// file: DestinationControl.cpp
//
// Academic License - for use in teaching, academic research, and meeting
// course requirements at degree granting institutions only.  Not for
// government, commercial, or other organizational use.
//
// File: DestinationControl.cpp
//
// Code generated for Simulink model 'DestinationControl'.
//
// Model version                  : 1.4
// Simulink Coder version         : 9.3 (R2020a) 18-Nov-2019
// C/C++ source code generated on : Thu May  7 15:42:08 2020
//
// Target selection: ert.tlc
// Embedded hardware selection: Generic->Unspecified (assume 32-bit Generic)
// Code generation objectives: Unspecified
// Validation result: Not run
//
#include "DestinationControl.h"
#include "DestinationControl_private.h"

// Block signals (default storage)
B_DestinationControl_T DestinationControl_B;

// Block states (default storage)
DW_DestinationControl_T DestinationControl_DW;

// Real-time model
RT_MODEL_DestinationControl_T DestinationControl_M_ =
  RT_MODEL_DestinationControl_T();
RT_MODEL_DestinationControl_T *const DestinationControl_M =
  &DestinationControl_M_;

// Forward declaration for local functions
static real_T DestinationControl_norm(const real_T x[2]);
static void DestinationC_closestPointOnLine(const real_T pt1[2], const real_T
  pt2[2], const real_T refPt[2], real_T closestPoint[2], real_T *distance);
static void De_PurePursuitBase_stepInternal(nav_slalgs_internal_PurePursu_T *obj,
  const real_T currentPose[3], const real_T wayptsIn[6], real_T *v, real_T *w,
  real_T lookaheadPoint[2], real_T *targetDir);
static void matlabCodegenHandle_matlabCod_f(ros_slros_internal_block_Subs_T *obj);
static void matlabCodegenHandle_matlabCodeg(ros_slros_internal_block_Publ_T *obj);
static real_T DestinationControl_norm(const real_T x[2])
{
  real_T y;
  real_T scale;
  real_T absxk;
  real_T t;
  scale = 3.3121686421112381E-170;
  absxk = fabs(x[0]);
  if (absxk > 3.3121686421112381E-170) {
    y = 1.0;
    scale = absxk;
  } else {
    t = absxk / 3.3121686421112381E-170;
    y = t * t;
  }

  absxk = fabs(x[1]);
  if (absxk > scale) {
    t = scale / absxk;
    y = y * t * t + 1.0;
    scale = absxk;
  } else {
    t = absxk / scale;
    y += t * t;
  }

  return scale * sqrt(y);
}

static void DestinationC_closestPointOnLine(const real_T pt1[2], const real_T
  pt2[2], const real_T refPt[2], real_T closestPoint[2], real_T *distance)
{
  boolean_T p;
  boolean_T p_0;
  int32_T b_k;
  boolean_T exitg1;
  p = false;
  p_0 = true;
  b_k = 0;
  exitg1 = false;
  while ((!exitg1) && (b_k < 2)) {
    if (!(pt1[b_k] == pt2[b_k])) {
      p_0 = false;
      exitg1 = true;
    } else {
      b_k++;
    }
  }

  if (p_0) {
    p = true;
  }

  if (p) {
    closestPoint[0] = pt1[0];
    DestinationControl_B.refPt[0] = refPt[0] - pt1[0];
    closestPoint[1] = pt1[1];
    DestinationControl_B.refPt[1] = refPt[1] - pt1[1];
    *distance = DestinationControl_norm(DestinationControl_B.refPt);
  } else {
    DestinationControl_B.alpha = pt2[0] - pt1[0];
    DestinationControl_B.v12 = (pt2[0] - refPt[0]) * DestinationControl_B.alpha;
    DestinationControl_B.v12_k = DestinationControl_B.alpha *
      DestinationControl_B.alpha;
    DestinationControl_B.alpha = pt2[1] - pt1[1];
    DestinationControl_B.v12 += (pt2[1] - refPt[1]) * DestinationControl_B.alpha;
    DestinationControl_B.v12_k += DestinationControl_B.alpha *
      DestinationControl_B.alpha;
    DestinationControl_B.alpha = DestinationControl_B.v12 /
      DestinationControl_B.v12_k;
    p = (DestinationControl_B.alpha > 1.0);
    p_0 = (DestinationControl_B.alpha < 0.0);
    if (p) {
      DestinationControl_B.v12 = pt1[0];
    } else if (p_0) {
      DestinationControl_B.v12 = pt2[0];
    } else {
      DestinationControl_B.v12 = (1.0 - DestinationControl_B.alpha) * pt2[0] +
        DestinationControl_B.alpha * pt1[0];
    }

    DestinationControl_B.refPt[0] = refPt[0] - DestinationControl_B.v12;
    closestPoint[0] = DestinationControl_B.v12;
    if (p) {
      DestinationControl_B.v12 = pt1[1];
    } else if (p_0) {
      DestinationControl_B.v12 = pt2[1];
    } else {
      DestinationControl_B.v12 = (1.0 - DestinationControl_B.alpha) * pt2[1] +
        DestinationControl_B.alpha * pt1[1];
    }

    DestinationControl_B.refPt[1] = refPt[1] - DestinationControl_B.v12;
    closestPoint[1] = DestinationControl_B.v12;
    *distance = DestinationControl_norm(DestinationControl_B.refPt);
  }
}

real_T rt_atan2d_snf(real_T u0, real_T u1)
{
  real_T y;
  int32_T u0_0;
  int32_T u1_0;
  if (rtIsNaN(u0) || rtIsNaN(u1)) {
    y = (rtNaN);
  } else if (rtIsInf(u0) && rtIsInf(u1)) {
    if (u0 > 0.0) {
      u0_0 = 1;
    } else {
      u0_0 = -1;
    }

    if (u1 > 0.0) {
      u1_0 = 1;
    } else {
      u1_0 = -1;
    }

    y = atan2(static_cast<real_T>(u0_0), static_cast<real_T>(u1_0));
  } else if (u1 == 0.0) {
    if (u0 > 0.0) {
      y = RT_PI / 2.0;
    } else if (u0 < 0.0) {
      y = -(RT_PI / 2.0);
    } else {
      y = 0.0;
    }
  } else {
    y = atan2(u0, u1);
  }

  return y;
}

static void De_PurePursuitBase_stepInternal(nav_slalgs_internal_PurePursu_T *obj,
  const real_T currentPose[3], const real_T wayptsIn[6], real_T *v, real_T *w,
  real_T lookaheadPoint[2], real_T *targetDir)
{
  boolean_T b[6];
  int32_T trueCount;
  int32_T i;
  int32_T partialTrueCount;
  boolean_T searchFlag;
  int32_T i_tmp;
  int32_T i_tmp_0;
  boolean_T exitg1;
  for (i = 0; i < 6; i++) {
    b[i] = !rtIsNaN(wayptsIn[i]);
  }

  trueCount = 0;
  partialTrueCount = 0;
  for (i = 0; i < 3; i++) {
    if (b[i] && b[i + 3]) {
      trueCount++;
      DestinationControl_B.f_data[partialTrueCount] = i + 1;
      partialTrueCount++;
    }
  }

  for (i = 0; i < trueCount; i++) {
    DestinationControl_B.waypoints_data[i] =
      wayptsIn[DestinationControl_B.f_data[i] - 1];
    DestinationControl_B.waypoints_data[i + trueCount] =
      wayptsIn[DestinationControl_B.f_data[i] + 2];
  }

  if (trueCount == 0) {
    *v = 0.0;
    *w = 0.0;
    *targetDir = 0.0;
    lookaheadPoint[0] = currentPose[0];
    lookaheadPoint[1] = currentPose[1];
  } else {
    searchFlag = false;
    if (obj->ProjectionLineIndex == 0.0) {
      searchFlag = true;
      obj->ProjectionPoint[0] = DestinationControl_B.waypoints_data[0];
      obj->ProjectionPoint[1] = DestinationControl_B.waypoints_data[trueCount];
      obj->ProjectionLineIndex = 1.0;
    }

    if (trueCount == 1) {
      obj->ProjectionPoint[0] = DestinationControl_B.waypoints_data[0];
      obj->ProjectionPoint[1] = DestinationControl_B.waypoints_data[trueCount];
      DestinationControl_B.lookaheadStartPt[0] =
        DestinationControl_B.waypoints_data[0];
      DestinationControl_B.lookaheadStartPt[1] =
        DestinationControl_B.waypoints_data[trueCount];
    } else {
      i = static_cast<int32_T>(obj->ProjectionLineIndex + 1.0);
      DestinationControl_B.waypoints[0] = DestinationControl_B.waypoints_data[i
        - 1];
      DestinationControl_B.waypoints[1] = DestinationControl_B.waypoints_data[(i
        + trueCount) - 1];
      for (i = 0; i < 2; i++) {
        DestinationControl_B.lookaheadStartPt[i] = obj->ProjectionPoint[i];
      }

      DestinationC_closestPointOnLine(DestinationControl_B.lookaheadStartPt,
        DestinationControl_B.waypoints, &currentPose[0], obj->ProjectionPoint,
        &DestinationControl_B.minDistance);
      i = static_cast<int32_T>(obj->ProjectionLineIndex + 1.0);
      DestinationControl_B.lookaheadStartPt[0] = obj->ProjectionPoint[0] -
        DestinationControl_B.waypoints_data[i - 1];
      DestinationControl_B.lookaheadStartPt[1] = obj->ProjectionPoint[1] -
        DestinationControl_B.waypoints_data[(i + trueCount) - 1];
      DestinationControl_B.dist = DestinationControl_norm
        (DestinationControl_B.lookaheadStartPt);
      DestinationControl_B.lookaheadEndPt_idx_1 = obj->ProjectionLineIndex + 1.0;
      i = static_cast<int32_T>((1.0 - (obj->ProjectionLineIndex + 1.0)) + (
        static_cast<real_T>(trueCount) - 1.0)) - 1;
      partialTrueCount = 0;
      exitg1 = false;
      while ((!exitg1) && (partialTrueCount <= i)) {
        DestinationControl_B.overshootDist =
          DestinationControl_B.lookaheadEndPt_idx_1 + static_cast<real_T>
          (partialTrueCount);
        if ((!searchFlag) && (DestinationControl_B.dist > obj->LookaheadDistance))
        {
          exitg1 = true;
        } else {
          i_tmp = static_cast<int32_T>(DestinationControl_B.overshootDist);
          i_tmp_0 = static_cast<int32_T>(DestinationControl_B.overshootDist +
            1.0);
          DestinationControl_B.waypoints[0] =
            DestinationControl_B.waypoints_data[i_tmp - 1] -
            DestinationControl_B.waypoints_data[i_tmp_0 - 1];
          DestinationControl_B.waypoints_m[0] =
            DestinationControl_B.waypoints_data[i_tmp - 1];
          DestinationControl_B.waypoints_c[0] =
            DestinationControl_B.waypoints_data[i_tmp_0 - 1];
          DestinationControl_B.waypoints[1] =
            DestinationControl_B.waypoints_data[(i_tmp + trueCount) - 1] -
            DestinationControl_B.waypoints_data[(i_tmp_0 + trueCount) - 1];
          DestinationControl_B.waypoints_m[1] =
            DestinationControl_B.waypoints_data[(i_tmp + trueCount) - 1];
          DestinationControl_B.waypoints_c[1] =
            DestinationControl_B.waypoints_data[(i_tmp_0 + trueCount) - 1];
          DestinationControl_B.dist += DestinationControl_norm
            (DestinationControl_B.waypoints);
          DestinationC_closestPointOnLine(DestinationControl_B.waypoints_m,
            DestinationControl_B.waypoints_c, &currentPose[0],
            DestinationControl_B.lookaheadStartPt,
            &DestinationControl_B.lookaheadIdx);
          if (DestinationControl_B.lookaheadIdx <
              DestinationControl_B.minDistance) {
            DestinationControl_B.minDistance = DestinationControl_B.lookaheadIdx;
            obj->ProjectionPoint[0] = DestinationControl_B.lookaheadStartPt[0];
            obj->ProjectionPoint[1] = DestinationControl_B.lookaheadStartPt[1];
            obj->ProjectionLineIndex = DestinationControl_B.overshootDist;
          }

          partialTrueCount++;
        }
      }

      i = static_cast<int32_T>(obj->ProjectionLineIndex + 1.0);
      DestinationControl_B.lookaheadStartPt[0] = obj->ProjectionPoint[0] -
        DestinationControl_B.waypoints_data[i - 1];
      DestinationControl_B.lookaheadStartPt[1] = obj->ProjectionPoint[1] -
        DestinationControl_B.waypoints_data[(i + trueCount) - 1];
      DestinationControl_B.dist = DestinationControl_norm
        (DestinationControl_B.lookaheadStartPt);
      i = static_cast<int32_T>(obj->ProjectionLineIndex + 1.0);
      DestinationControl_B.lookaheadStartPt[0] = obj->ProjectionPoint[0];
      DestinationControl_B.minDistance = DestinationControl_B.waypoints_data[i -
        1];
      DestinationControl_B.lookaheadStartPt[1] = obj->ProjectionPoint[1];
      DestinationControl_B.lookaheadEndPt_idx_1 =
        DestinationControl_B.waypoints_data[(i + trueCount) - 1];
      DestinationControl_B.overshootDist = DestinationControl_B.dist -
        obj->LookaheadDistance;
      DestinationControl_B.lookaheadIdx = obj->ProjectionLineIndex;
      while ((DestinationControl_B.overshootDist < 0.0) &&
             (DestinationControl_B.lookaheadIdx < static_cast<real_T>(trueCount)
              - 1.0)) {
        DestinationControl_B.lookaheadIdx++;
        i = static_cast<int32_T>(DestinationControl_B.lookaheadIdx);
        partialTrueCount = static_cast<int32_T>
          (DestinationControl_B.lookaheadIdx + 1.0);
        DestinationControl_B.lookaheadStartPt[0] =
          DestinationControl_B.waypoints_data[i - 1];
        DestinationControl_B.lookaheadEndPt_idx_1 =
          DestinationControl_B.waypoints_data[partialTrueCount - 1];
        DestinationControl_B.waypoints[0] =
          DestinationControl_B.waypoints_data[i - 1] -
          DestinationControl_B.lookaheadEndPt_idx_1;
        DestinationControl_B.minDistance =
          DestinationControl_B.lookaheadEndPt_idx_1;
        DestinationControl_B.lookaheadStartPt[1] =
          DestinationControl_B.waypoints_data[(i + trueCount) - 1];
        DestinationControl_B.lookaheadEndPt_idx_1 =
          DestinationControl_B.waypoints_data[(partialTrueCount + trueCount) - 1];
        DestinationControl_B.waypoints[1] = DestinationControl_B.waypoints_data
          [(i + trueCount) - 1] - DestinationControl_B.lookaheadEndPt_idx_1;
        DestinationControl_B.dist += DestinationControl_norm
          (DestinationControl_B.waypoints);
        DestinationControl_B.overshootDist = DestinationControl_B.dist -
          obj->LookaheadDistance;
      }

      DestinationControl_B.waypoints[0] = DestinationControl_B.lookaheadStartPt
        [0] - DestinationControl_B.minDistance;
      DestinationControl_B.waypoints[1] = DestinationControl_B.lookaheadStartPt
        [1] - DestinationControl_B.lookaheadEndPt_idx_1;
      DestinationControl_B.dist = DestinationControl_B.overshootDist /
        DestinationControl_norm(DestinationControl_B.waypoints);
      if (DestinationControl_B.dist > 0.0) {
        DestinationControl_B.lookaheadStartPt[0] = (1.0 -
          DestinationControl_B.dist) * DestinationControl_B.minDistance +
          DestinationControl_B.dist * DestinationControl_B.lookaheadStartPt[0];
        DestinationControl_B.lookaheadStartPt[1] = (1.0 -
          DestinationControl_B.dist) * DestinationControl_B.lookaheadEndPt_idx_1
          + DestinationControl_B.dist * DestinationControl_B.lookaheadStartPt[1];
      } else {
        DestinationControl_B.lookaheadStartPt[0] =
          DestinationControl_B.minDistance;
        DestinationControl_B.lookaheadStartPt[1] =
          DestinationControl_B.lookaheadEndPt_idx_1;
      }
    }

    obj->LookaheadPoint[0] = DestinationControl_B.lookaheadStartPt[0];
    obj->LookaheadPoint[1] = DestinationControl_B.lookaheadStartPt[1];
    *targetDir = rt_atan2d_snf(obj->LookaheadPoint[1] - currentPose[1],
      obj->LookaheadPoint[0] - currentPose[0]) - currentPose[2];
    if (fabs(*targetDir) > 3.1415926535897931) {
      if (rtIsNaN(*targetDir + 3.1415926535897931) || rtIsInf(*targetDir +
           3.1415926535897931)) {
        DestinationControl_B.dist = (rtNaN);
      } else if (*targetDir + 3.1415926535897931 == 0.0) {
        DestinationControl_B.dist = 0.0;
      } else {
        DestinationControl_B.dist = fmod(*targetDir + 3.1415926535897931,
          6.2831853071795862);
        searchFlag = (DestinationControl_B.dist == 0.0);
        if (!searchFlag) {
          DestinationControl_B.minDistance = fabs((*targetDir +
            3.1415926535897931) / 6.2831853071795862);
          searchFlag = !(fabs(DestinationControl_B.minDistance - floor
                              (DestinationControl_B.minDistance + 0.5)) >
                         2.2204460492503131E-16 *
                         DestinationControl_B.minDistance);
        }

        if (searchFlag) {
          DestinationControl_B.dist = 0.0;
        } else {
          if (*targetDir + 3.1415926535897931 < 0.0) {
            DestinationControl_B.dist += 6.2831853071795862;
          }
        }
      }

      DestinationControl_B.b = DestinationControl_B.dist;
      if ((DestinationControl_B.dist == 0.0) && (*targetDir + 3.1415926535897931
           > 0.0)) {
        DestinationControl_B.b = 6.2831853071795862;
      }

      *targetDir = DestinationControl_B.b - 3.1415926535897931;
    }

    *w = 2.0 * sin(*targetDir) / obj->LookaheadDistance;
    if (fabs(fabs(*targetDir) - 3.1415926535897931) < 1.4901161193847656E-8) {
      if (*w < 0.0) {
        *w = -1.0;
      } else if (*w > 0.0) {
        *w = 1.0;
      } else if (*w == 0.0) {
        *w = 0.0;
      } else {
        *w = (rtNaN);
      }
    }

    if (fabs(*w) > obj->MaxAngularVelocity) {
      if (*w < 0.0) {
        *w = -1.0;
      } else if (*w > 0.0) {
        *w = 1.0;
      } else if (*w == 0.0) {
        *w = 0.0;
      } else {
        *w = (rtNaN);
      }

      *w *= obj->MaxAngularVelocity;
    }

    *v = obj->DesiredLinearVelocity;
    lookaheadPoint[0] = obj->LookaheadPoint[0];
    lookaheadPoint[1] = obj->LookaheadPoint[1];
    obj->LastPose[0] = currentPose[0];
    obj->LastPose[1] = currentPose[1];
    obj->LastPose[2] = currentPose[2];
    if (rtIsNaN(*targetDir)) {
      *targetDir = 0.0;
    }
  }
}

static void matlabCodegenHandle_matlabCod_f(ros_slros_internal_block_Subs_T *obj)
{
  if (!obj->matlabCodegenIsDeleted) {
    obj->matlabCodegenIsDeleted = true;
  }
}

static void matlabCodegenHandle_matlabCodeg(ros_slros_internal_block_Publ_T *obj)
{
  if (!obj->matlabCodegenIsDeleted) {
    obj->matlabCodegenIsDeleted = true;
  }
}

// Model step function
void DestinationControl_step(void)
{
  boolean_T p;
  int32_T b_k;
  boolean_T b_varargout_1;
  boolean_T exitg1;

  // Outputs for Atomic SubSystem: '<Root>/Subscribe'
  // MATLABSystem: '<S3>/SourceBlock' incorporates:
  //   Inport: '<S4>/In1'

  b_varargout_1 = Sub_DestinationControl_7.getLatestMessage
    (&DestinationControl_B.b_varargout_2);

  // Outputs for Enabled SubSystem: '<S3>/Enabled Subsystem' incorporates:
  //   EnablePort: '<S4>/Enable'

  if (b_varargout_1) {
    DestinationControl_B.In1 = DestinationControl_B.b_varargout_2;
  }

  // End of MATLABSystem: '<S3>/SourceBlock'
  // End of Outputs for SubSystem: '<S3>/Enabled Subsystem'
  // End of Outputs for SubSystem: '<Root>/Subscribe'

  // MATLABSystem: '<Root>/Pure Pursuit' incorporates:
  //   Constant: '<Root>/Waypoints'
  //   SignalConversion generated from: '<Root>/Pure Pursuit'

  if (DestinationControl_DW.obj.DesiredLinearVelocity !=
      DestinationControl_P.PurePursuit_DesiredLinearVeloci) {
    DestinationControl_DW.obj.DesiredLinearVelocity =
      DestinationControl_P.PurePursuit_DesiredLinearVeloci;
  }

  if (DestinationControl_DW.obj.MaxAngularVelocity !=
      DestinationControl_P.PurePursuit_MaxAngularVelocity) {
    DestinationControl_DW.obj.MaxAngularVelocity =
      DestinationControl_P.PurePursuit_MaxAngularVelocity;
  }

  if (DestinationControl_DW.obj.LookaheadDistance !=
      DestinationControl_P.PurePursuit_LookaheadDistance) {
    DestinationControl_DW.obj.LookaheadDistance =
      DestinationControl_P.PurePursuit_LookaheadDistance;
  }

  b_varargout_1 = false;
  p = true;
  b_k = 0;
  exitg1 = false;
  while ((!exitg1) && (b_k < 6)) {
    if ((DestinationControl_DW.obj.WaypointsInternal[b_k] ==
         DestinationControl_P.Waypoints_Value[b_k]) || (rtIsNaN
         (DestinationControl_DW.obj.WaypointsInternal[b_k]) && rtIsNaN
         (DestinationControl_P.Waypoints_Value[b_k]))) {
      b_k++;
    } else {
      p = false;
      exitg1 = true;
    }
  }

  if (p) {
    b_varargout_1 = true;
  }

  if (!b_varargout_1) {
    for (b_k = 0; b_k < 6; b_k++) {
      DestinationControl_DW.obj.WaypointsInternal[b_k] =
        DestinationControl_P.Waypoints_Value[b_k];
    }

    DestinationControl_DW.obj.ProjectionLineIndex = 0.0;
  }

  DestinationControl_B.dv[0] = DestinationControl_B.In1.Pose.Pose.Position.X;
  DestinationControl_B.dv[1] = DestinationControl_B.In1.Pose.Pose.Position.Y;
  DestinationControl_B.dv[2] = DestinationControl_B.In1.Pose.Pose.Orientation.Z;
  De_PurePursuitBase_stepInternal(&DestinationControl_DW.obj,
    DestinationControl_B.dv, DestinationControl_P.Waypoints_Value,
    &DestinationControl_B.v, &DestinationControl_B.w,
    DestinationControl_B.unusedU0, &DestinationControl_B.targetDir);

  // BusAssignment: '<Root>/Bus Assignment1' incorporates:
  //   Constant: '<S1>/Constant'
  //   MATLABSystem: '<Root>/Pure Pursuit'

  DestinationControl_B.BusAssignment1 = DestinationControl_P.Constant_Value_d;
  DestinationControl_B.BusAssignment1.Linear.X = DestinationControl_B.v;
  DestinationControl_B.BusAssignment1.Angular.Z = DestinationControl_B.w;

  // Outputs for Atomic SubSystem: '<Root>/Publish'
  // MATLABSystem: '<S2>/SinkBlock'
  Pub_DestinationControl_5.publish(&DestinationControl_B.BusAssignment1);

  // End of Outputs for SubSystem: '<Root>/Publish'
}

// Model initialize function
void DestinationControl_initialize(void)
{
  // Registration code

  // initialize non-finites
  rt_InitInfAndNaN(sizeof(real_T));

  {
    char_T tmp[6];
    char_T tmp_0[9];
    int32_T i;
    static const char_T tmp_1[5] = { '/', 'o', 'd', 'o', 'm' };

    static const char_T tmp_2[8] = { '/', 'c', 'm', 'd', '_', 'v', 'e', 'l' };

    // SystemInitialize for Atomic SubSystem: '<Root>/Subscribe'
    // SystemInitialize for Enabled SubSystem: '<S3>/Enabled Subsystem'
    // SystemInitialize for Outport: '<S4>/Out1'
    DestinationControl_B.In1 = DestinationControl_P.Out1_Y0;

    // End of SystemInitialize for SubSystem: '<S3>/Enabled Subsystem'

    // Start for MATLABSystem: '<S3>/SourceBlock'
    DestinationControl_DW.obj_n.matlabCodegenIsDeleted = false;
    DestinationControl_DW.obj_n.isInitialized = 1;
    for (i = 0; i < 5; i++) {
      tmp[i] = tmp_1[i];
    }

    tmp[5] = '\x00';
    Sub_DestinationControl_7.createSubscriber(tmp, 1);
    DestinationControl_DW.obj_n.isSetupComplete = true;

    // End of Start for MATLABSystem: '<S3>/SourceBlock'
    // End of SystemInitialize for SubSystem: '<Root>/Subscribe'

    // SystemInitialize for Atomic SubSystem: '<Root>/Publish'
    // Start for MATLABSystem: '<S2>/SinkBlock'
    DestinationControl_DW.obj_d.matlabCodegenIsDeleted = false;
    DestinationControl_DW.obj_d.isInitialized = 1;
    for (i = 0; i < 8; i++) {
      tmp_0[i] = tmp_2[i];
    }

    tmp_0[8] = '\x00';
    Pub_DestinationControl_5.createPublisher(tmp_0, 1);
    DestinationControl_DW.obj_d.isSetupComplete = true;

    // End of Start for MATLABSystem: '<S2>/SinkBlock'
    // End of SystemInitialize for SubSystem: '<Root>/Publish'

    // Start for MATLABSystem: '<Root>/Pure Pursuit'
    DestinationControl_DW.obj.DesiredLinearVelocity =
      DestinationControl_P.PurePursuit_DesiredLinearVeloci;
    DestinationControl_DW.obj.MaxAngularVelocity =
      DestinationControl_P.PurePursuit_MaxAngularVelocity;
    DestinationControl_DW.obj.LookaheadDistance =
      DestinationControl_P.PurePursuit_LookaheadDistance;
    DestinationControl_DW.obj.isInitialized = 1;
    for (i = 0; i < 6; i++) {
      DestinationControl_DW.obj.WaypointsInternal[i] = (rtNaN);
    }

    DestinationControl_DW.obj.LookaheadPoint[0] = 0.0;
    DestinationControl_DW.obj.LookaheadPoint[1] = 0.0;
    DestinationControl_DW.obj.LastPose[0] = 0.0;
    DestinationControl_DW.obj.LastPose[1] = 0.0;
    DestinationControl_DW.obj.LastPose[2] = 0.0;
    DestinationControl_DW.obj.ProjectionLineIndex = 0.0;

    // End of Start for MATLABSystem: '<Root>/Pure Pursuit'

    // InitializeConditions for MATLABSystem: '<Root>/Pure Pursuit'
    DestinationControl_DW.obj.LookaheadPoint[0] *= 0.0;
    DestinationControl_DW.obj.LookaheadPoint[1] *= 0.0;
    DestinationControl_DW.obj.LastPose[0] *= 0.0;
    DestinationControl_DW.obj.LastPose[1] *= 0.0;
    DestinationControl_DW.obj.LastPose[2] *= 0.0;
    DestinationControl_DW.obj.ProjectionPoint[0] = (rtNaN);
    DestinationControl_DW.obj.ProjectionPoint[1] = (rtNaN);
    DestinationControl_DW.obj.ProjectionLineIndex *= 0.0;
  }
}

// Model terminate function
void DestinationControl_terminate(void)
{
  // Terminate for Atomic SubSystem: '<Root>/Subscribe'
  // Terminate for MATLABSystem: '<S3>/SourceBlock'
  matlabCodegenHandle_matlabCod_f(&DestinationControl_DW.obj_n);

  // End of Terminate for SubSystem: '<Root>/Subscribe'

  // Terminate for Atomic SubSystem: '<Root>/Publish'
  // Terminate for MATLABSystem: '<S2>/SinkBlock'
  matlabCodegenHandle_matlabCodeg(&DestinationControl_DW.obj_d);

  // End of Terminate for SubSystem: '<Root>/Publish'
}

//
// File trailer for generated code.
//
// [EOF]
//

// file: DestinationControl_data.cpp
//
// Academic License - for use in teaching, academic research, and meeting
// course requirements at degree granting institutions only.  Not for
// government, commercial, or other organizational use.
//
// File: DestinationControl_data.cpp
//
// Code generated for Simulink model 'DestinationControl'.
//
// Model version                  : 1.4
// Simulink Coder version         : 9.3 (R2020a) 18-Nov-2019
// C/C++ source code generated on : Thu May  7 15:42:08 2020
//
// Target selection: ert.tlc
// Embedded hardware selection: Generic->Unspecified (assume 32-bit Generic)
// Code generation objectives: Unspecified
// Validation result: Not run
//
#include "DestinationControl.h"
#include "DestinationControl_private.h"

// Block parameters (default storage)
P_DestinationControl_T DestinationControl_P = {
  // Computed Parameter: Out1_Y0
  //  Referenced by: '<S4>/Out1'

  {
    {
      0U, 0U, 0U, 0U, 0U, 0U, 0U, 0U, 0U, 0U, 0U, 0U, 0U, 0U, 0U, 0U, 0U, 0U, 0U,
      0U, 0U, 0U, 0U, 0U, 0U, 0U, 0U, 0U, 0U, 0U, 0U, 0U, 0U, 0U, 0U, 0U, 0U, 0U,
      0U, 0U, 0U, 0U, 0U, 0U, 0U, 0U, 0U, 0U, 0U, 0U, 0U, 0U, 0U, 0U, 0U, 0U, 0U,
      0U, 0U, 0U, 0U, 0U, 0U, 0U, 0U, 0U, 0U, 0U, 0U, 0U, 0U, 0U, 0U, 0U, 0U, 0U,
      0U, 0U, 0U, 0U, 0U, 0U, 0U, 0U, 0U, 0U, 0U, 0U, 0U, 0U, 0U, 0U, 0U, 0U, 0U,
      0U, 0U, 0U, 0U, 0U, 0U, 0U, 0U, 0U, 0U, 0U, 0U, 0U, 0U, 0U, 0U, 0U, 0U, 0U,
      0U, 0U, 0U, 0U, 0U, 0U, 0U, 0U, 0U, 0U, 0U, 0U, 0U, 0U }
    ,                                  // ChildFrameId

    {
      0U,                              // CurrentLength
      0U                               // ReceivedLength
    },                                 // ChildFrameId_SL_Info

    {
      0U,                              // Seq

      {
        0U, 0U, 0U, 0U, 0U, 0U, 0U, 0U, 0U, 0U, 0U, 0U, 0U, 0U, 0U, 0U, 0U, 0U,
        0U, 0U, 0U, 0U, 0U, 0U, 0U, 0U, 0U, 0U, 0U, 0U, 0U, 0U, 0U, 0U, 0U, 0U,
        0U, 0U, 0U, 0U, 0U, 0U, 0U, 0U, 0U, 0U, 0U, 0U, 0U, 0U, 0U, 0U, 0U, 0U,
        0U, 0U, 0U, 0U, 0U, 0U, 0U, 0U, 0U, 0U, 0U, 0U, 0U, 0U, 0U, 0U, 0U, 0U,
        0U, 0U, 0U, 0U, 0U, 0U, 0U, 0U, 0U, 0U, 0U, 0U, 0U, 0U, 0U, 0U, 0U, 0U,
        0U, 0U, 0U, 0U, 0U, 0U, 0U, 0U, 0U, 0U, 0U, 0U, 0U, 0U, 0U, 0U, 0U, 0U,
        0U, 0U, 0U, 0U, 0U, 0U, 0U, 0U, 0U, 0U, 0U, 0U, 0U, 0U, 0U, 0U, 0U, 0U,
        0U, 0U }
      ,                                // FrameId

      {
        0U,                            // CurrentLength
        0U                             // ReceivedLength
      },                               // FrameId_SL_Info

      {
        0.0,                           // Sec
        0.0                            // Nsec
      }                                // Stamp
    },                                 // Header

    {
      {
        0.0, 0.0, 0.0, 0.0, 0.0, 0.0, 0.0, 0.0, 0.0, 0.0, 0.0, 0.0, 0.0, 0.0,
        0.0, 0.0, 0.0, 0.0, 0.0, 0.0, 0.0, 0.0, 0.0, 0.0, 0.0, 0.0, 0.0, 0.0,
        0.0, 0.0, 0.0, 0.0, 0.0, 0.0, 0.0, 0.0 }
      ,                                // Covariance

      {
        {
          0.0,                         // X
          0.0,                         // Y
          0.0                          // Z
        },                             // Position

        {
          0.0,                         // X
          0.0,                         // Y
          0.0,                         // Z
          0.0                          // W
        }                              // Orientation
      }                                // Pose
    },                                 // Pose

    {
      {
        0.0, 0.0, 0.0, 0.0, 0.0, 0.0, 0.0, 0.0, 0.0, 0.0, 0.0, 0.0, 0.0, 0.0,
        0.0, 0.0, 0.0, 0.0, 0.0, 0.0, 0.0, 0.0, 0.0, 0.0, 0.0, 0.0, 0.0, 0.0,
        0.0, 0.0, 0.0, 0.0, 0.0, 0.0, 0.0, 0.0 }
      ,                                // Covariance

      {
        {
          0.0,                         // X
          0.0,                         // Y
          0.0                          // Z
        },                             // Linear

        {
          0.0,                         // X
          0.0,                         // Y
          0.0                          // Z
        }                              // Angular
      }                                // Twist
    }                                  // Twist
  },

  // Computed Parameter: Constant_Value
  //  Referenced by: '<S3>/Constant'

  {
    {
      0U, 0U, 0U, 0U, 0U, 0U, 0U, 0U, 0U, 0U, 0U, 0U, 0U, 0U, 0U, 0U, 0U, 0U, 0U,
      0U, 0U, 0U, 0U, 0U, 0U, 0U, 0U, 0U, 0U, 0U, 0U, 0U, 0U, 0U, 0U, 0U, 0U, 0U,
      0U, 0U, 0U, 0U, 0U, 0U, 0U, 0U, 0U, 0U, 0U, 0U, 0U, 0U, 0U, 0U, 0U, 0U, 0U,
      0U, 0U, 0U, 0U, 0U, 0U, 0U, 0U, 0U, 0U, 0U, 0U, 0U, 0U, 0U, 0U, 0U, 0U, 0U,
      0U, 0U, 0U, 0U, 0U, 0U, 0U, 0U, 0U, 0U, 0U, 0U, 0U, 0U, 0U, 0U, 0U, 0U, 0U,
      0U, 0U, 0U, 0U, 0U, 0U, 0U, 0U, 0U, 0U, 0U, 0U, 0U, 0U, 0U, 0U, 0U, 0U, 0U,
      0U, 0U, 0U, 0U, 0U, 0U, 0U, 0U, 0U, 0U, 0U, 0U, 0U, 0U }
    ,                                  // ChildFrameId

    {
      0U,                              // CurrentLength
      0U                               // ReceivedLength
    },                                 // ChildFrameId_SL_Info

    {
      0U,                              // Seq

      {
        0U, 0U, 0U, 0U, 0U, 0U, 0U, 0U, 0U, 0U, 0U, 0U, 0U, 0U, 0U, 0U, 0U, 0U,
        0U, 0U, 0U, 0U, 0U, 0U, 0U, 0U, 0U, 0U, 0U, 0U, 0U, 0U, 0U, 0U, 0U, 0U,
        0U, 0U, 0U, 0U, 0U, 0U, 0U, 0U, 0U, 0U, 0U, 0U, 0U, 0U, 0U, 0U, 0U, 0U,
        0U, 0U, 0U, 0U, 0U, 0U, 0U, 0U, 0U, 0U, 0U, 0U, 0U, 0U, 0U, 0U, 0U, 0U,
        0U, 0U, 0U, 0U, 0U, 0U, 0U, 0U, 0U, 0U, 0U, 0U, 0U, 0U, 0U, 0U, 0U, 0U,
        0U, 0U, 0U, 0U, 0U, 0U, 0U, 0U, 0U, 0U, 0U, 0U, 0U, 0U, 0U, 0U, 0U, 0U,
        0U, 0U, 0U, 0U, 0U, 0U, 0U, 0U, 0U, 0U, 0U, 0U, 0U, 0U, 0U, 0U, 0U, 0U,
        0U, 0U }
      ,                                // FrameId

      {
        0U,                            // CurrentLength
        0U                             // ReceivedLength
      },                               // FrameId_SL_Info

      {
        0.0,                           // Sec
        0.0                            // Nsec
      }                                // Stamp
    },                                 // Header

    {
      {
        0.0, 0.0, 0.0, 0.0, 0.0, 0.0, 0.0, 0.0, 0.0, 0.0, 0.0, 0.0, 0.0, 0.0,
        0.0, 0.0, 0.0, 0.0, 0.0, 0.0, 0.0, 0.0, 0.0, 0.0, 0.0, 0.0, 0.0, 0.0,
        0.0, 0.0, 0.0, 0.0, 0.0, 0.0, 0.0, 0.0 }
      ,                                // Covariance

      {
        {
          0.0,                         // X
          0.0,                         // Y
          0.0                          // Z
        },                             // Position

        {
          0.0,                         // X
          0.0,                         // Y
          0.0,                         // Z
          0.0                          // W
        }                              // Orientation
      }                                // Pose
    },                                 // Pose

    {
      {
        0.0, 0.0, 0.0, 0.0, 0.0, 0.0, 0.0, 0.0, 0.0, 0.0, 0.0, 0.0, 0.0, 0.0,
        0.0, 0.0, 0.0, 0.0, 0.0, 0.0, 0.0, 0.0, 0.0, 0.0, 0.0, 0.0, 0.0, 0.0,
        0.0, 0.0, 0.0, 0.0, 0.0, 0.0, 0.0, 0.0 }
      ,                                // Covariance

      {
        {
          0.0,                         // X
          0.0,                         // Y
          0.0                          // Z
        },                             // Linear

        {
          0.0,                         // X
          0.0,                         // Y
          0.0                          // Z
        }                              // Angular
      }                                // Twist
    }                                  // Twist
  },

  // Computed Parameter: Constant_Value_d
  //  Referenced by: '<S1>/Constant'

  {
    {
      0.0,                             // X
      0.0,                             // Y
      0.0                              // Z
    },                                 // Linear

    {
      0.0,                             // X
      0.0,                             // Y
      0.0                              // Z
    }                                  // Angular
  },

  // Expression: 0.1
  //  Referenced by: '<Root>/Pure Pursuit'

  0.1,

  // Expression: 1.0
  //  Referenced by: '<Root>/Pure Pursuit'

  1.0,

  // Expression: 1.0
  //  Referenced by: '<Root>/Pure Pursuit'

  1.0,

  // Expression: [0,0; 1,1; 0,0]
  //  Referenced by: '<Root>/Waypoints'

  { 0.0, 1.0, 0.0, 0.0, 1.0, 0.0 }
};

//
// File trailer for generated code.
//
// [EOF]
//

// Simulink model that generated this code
simulink model "DestinationControl"  (R2020a)
settings: Solver=ode3  StartTime=0.0  StopTime=10.0  RelTol=1e-3
PreLoadFcn:
  | % Lidar parameters
  | 
  | scanAngles = linspace(-pi/2,pi/2,360);
  | scanMaxRange = 3.5;
  | scanSensorOffset = [0,0];
undefined symbols (not defined in the file or in its folder): Angular, Linear
libraries: robotlib x5, robotalgslib x1

== system DestinationControl ==
  note: Destination Algorithm
      | (Differential Drive)
      |
      | Franklin Team
  Blank Message : robotlib/Blank Message  messageClass=Message  entityType=geometry_msgs/Twist  messageType=geometry_msgs/Twist  SampleTime=inf
  Bus Assignment1 : BusAssignment  AssignedSignals=Linear.X,Angular.Z
  Bus Selector : BusSelector  OutputSignals=Pose.Pose.Position.X,Pose.Pose.Position.Y,Pose.Pose.Orientation.Z
  Bus Selector1 : BusSelector  Commented=on  OutputSignals=X,Y
  Bus Selector2 : BusSelector  Commented=on  OutputSignals=Ranges,Intensities
  Matrix Concatenate : Concatenate  Commented=on  Mode=Multidimensional array  ConcatenateDimension=2
  Mux : Mux  Inputs=3
  Mux1 : Mux  Commented=on  Inputs=1
  Publish : robotlib/Publish  topicSource=Specify your own  topic=/cmd_vel  messageType=geometry_msgs/Twist  messageQueueLength=1
  Pure Pursuit : robotalgslib/Pure Pursuit  DesiredLinearVelocity=0.1  MaxAngularVelocity=1.0  LookaheadDistance=1.0  TargetDirPort=off  SimulateUsing=Code generation
  Subscribe : robotlib/Subscribe  topicSource=Specify your own  topic=/odom  messageType=nav_msgs/Odometry  sampleTime=-1  messageQueueLength=1
  Subscribe1 : robotlib/Subscribe  Commented=on  topicSource=Specify your own  topic=/destination  messageType=geometry_msgs/Point  sampleTime=-1  messageQueueLength=1
  Subscribe2 : robotlib/Subscribe  Commented=on  topicSource=Specify your own  topic=/scan  messageType=sensor_msgs/LaserScan  sampleTime=-1  messageQueueLength=1
  Transpose : Math  Commented=on  Operator=transpose  SignedPower=on  RndMeth=Zero  SaturateOnIntegerOverflow=on
  Vector Concatenate : Concatenate  Commented=on  ConcatenateDimension=2
  Waypoints : Constant  Value=[0,0; 1,1; 0,0]
  wires:
  Subscribe/2 -> Bus Selector/1
  Blank Message/1 -> Bus Assignment1/1
  Bus Selector/1 -> Mux/1  "<X>"
  Bus Selector/2 -> Mux/2  "<Y>"
  Bus Selector/3 -> Mux/3  "<Z>"
  Subscribe1/2 -> Bus Selector1/1
  Bus Selector1/1 -> Vector Concatenate/1  "<X>"
  Bus Selector1/2 -> Vector Concatenate/2  "<Y>"
  Matrix Concatenate/1 -> Transpose/1
  Vector Concatenate/1 -> Matrix Concatenate/2  "waypoints"
  Bus Assignment1/1 -> Publish/1
  Pure Pursuit/1 -> Bus Assignment1/2  "v"
  Mux/1 -> Pure Pursuit/1
  Waypoints/1 -> Pure Pursuit/2  "waypoints"
  Subscribe2/2 -> Bus Selector2/1
  Bus Selector2/1 -> Mux1/1  "<Ranges>"
  Mux1/1 -> ?
  Bus Selector2/2 -> ?  "<Intensities>"
  Pure Pursuit/2 -> Bus Assignment1/3
